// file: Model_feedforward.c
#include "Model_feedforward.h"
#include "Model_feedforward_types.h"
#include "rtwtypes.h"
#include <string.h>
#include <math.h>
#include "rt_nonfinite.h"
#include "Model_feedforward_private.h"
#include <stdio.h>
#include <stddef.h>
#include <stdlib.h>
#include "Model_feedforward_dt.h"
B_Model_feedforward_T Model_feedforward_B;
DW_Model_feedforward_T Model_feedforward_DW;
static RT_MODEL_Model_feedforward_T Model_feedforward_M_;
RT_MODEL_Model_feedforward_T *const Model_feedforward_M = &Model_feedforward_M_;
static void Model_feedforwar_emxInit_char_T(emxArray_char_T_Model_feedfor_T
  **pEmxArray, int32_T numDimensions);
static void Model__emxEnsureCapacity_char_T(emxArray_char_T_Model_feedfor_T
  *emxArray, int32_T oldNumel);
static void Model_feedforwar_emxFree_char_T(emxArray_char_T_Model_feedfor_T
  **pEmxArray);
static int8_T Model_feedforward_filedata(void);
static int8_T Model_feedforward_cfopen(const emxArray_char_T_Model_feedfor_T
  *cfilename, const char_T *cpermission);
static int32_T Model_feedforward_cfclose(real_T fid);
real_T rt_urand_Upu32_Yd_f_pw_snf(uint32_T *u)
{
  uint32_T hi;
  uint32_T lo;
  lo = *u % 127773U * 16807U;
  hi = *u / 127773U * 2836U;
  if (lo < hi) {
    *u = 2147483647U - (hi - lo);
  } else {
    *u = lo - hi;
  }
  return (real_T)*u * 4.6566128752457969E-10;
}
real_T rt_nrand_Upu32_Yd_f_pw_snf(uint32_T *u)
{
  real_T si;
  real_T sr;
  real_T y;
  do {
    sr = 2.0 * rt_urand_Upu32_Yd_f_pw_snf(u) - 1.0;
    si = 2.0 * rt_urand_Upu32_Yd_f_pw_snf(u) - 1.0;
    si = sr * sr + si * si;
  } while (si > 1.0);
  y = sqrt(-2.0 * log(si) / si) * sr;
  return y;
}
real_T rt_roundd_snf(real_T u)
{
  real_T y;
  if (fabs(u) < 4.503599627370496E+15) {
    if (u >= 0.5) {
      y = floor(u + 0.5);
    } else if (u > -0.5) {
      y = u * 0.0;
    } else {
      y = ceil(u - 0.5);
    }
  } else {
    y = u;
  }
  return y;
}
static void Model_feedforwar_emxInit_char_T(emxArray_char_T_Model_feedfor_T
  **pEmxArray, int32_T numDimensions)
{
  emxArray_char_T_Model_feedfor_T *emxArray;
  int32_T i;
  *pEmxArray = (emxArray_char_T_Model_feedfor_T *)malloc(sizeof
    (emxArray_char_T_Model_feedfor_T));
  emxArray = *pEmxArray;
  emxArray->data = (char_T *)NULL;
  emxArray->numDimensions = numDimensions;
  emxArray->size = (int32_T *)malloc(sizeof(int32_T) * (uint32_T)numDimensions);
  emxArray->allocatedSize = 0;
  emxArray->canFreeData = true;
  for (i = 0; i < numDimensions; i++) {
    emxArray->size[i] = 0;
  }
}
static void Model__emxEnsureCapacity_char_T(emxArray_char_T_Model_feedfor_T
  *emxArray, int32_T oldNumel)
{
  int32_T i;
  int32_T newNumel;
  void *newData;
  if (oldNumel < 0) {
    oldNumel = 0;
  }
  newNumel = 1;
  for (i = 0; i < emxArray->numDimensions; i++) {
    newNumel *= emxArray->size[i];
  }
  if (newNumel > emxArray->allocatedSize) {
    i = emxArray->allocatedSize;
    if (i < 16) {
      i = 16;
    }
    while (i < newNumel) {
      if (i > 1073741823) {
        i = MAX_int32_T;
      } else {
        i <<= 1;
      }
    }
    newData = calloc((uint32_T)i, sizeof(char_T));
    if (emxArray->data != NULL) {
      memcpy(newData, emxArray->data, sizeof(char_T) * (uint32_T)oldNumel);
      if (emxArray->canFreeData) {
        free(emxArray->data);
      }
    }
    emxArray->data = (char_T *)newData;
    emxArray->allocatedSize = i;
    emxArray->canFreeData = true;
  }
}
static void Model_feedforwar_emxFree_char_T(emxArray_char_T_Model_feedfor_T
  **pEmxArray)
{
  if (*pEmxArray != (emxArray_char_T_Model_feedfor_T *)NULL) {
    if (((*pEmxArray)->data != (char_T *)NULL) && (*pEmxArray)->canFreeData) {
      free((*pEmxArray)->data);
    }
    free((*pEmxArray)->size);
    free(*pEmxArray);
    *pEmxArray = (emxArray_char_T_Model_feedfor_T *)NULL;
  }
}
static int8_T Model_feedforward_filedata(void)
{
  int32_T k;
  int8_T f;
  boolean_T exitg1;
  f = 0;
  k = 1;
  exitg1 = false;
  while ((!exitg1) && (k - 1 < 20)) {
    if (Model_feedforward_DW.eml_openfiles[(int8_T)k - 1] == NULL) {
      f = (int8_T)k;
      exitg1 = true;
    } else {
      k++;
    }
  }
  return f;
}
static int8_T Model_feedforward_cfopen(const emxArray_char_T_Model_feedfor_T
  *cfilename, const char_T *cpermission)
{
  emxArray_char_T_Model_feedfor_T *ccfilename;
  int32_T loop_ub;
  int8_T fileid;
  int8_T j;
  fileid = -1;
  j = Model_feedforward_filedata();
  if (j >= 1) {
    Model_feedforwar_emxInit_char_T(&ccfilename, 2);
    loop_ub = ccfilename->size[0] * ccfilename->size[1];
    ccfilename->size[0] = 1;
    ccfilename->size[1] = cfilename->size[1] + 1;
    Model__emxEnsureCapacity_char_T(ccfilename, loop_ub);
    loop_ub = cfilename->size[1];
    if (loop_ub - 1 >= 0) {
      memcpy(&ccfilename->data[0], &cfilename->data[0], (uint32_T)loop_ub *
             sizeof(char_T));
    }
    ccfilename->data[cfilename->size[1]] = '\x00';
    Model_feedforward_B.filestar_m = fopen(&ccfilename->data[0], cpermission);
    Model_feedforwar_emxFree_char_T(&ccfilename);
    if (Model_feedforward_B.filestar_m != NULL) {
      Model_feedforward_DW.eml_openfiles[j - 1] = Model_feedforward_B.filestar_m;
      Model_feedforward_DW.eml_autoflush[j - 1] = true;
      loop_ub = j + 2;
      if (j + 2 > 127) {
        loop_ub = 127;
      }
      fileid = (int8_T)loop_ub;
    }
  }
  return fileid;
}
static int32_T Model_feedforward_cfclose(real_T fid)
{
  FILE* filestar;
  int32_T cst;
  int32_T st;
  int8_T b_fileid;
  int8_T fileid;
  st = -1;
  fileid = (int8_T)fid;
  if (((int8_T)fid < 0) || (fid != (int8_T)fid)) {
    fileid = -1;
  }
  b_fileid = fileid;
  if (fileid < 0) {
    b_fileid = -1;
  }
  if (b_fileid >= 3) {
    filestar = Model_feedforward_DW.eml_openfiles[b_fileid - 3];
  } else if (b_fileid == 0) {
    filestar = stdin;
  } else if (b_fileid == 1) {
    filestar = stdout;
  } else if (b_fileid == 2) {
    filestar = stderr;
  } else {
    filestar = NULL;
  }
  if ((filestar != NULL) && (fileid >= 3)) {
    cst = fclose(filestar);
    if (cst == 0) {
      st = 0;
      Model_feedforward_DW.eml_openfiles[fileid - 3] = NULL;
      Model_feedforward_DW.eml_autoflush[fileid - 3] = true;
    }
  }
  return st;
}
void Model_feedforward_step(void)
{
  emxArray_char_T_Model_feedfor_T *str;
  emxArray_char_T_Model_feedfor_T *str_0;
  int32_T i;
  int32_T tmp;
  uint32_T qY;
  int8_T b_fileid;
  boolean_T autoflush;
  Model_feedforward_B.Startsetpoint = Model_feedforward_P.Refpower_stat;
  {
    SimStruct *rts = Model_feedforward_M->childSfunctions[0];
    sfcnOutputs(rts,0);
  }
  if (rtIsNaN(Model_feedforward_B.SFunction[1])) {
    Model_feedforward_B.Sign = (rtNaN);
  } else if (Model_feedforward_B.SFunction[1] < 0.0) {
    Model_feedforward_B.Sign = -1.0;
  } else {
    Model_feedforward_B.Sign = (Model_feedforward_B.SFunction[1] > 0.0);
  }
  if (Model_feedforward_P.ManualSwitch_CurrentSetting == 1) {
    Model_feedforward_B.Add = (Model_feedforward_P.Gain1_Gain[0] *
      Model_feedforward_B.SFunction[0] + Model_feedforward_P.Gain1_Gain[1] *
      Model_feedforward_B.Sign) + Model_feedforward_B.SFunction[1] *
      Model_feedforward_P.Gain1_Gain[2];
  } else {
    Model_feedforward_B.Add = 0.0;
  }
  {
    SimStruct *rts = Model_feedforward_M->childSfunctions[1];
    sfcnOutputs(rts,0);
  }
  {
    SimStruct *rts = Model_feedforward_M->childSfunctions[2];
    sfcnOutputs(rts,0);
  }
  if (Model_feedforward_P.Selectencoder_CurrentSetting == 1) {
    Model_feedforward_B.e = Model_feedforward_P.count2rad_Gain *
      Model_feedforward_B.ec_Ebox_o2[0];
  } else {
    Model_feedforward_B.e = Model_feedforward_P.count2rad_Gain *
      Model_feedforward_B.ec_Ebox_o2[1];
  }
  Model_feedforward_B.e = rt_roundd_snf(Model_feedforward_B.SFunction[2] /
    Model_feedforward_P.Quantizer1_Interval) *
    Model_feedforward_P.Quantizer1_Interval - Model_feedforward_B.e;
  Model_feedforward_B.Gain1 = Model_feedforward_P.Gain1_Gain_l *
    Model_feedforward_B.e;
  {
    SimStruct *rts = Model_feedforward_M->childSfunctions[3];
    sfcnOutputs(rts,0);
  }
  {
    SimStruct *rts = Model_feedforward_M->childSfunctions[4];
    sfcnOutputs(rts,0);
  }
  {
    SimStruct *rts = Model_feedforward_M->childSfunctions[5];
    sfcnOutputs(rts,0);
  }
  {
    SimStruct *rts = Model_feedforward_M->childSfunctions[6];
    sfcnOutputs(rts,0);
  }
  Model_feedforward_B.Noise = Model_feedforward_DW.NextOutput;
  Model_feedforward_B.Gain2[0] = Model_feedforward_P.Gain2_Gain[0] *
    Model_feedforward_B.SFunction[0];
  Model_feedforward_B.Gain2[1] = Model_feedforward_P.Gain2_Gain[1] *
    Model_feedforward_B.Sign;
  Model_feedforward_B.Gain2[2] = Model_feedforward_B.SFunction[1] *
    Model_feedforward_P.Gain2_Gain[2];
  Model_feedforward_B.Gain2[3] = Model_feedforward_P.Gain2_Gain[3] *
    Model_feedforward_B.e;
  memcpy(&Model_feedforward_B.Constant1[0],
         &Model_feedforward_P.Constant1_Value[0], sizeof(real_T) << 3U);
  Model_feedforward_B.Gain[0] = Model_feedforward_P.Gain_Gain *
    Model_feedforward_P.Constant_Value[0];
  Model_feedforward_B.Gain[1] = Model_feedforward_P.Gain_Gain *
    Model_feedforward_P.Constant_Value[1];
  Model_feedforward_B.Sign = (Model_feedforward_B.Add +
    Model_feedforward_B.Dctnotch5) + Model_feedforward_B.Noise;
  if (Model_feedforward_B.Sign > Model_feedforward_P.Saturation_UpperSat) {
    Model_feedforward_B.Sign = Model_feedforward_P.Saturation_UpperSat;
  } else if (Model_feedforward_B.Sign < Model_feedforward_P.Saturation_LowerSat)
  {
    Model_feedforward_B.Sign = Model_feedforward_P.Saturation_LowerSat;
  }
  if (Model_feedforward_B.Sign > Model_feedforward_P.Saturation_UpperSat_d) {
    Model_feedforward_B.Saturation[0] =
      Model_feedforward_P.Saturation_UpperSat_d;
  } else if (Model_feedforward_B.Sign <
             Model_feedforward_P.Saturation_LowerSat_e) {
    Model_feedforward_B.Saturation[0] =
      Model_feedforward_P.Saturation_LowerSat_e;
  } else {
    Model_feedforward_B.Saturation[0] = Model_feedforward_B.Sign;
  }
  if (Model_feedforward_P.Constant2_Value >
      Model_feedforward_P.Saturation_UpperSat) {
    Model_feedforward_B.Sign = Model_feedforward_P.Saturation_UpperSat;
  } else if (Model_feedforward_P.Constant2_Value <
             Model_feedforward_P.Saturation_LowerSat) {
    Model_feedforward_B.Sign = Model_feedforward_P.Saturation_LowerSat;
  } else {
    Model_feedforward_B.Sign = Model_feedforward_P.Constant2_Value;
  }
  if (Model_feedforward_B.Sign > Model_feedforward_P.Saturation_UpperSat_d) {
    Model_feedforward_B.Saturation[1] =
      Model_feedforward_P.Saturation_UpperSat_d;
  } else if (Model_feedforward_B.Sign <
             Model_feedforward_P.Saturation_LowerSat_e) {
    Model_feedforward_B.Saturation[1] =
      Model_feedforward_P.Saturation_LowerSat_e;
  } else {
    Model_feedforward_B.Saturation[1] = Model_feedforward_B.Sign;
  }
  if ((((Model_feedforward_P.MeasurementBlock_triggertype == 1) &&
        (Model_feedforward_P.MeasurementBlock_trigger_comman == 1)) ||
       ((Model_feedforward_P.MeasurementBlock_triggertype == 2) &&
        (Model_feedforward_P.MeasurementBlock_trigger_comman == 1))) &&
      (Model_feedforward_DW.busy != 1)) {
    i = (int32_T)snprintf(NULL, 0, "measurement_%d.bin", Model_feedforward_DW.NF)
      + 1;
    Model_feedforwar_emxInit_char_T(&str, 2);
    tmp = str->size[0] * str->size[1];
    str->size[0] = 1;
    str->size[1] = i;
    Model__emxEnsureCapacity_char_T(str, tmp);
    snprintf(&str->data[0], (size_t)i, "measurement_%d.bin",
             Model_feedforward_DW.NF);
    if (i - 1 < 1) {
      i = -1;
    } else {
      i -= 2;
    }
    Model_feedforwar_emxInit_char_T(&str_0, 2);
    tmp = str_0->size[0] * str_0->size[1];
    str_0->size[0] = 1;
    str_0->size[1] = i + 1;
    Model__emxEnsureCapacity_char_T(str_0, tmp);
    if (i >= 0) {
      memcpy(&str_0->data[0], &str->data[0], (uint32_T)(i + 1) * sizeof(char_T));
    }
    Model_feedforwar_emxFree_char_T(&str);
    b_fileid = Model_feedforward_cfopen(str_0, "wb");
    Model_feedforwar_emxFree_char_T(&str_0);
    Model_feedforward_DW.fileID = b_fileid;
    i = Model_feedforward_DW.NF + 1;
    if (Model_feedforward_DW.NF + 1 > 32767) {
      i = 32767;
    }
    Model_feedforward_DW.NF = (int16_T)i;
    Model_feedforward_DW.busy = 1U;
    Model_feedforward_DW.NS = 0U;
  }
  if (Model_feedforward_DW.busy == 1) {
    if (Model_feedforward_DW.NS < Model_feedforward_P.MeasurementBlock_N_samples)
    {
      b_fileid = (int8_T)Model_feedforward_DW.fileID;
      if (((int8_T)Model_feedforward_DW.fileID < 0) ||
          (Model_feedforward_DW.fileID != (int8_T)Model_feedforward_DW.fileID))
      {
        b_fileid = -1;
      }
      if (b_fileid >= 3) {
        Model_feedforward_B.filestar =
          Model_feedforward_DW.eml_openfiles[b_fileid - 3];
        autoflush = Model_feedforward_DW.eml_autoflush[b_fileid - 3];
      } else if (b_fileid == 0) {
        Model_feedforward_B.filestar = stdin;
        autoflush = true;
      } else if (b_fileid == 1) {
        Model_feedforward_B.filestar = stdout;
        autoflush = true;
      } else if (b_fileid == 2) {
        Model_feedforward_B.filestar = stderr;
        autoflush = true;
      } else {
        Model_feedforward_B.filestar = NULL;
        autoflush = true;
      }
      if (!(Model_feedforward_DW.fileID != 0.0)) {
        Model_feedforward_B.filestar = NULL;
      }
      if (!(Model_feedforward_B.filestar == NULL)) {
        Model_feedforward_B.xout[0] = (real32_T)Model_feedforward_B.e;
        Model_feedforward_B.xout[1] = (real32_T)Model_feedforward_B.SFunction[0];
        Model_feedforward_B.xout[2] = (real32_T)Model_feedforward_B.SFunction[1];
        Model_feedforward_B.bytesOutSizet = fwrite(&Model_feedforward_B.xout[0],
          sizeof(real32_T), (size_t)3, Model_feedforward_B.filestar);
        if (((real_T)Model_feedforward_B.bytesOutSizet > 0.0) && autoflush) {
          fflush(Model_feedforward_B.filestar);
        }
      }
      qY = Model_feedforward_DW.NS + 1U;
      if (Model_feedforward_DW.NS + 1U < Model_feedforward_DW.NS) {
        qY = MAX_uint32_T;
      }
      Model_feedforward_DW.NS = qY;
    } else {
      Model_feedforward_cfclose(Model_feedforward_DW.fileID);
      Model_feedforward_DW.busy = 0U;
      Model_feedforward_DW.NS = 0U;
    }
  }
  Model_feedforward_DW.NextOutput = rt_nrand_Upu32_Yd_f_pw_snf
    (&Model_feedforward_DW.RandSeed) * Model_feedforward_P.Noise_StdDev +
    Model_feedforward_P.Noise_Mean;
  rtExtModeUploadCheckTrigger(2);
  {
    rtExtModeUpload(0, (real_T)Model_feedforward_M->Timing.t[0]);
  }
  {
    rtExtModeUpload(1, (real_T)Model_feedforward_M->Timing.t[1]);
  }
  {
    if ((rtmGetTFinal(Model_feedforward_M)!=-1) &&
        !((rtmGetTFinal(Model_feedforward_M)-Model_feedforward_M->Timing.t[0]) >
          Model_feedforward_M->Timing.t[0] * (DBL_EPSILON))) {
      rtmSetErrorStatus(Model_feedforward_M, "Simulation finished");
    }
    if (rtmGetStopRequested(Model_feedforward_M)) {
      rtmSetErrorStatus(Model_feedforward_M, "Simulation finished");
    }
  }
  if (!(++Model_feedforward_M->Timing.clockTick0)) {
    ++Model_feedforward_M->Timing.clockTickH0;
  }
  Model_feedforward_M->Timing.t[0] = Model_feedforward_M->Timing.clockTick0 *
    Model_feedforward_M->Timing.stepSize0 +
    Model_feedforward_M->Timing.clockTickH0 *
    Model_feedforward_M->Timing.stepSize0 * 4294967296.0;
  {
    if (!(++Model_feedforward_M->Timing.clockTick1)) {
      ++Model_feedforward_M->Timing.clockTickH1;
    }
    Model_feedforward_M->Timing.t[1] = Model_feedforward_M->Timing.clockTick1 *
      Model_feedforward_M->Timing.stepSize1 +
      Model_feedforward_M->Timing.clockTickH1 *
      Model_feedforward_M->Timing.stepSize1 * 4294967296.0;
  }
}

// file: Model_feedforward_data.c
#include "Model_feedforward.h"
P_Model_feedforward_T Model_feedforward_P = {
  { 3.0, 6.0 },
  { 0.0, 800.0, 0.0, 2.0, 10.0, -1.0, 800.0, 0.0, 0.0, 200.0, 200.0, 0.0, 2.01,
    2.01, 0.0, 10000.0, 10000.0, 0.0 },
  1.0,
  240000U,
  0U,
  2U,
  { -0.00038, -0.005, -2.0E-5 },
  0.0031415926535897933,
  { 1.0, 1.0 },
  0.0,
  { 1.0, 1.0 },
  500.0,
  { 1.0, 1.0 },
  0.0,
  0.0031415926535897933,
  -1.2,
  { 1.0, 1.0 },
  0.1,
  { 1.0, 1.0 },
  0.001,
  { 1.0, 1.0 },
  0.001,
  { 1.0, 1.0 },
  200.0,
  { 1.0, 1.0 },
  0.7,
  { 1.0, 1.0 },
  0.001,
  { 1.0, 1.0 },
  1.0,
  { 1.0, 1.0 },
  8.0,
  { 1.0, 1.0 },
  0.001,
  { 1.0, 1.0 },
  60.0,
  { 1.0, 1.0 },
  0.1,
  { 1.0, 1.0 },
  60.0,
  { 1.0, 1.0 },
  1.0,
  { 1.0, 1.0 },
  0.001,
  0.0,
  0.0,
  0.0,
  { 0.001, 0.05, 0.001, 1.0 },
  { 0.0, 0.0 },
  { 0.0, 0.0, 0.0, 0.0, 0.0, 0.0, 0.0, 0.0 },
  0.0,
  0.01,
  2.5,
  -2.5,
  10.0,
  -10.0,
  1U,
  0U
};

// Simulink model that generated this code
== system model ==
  MATLABFunction#1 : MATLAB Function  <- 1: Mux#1, 3: Constant#1, 4: Constant#2
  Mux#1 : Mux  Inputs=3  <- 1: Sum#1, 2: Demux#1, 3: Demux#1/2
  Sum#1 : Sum  Inputs=+-  <- 1: Quantizer1, 2: Selectencoder
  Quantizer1 : Quantizer  QuantizationInterval=(2*pi)/(500*4)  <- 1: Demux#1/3
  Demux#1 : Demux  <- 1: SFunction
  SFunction : S-Function  FunctionName=ref3b  <- 1: Startsetpoint
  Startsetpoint : Constant  Value=stat
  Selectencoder : ManualSwitch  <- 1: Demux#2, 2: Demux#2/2
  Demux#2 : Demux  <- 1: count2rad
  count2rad : Gain  Gain=(2*pi)/(4*500)  <- 1: ec_Ebox/2
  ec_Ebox : S-Function  FunctionName=ec_Ebox  <- 1: Saturation, 2: Gain, 3: Constant1
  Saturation : Saturate  UpperLimit=10  LowerLimit=-10  <- 1: Saturate#1
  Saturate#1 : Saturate  UpperLimit=2.5  LowerLimit=-2.5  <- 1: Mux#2
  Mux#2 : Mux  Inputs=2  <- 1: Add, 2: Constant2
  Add : Sum  Inputs=+++  <- 1: ManualSwitch, 2: Dct2lowpass#1, 3: Noise
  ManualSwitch : ManualSwitch  <- 1: Gain1
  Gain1 : Gain  Gain=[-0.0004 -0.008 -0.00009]  Multiplication=Matrix(K*u)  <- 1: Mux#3
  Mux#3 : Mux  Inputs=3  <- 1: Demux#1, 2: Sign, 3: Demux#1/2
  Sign : Signum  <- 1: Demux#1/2
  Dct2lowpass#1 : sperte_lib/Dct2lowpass  <- 1: Dctpd#1
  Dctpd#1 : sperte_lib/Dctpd  <- 1: Gain#1
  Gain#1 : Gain  Gain=-1  <- 1: Sum#1
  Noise : RandomNumber
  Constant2 : Constant  Value=0
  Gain : Gain  Gain=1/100  <- 1: Constant
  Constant : Constant  Value=[0,0]
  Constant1 : Constant  Value=[0,0,0,0,0,0,0,0]
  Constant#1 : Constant  Value=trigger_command
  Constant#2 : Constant  Value=N_samples
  SFunction#1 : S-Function  FunctionName=ec_Supervisor
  Gain2 : Gain  Gain=[0.001 0.05 0.001 1]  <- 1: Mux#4
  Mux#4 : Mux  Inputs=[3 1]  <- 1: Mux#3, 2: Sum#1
== matlab function MATLABFunction#1 ==
function status = perform_measurement(u, trigger_manual, trigger_command, triggertype, N_samples)

%% Persistent variables
persistent fileID NF busy NS

% Init parameters
if isempty(NF)
    NF = int16(0);
end
if isempty(NS)
    NS = uint32(0);
end
if isempty(fileID)
    fileID = 0;
end
if isempty(busy)
    busy = uint8(0);
end

%% Check the triggers
if ( (triggertype == 0 && trigger_manual == 1) || (triggertype == 1 && trigger_command == 1) || (triggertype == 2 && (trigger_command == 1 || trigger_manual == 1) ) )
    if busy == 1
        % We are already busy, nothing to do
    else
        % We should start a new one
        fileID = fopen(sprintf('measurement_%d.bin',NF),'w');  
        NF = NF + 1;
        busy = uint8(1);
        NS = uint32(0);
    end
end

% We have started a measurement
if busy == 1
    if NS < N_samples 
        % Here we write the sample, in single precision float
        fwrite(fileID,u,'single');
        NS = NS + uint32(1);
    else
       % We have N samples already, we are done
       fclose(fileID);
       busy = uint8(0);
       NS = uint32(0);
    end
      
end
    % Output state
    status = uint8(busy);
end
